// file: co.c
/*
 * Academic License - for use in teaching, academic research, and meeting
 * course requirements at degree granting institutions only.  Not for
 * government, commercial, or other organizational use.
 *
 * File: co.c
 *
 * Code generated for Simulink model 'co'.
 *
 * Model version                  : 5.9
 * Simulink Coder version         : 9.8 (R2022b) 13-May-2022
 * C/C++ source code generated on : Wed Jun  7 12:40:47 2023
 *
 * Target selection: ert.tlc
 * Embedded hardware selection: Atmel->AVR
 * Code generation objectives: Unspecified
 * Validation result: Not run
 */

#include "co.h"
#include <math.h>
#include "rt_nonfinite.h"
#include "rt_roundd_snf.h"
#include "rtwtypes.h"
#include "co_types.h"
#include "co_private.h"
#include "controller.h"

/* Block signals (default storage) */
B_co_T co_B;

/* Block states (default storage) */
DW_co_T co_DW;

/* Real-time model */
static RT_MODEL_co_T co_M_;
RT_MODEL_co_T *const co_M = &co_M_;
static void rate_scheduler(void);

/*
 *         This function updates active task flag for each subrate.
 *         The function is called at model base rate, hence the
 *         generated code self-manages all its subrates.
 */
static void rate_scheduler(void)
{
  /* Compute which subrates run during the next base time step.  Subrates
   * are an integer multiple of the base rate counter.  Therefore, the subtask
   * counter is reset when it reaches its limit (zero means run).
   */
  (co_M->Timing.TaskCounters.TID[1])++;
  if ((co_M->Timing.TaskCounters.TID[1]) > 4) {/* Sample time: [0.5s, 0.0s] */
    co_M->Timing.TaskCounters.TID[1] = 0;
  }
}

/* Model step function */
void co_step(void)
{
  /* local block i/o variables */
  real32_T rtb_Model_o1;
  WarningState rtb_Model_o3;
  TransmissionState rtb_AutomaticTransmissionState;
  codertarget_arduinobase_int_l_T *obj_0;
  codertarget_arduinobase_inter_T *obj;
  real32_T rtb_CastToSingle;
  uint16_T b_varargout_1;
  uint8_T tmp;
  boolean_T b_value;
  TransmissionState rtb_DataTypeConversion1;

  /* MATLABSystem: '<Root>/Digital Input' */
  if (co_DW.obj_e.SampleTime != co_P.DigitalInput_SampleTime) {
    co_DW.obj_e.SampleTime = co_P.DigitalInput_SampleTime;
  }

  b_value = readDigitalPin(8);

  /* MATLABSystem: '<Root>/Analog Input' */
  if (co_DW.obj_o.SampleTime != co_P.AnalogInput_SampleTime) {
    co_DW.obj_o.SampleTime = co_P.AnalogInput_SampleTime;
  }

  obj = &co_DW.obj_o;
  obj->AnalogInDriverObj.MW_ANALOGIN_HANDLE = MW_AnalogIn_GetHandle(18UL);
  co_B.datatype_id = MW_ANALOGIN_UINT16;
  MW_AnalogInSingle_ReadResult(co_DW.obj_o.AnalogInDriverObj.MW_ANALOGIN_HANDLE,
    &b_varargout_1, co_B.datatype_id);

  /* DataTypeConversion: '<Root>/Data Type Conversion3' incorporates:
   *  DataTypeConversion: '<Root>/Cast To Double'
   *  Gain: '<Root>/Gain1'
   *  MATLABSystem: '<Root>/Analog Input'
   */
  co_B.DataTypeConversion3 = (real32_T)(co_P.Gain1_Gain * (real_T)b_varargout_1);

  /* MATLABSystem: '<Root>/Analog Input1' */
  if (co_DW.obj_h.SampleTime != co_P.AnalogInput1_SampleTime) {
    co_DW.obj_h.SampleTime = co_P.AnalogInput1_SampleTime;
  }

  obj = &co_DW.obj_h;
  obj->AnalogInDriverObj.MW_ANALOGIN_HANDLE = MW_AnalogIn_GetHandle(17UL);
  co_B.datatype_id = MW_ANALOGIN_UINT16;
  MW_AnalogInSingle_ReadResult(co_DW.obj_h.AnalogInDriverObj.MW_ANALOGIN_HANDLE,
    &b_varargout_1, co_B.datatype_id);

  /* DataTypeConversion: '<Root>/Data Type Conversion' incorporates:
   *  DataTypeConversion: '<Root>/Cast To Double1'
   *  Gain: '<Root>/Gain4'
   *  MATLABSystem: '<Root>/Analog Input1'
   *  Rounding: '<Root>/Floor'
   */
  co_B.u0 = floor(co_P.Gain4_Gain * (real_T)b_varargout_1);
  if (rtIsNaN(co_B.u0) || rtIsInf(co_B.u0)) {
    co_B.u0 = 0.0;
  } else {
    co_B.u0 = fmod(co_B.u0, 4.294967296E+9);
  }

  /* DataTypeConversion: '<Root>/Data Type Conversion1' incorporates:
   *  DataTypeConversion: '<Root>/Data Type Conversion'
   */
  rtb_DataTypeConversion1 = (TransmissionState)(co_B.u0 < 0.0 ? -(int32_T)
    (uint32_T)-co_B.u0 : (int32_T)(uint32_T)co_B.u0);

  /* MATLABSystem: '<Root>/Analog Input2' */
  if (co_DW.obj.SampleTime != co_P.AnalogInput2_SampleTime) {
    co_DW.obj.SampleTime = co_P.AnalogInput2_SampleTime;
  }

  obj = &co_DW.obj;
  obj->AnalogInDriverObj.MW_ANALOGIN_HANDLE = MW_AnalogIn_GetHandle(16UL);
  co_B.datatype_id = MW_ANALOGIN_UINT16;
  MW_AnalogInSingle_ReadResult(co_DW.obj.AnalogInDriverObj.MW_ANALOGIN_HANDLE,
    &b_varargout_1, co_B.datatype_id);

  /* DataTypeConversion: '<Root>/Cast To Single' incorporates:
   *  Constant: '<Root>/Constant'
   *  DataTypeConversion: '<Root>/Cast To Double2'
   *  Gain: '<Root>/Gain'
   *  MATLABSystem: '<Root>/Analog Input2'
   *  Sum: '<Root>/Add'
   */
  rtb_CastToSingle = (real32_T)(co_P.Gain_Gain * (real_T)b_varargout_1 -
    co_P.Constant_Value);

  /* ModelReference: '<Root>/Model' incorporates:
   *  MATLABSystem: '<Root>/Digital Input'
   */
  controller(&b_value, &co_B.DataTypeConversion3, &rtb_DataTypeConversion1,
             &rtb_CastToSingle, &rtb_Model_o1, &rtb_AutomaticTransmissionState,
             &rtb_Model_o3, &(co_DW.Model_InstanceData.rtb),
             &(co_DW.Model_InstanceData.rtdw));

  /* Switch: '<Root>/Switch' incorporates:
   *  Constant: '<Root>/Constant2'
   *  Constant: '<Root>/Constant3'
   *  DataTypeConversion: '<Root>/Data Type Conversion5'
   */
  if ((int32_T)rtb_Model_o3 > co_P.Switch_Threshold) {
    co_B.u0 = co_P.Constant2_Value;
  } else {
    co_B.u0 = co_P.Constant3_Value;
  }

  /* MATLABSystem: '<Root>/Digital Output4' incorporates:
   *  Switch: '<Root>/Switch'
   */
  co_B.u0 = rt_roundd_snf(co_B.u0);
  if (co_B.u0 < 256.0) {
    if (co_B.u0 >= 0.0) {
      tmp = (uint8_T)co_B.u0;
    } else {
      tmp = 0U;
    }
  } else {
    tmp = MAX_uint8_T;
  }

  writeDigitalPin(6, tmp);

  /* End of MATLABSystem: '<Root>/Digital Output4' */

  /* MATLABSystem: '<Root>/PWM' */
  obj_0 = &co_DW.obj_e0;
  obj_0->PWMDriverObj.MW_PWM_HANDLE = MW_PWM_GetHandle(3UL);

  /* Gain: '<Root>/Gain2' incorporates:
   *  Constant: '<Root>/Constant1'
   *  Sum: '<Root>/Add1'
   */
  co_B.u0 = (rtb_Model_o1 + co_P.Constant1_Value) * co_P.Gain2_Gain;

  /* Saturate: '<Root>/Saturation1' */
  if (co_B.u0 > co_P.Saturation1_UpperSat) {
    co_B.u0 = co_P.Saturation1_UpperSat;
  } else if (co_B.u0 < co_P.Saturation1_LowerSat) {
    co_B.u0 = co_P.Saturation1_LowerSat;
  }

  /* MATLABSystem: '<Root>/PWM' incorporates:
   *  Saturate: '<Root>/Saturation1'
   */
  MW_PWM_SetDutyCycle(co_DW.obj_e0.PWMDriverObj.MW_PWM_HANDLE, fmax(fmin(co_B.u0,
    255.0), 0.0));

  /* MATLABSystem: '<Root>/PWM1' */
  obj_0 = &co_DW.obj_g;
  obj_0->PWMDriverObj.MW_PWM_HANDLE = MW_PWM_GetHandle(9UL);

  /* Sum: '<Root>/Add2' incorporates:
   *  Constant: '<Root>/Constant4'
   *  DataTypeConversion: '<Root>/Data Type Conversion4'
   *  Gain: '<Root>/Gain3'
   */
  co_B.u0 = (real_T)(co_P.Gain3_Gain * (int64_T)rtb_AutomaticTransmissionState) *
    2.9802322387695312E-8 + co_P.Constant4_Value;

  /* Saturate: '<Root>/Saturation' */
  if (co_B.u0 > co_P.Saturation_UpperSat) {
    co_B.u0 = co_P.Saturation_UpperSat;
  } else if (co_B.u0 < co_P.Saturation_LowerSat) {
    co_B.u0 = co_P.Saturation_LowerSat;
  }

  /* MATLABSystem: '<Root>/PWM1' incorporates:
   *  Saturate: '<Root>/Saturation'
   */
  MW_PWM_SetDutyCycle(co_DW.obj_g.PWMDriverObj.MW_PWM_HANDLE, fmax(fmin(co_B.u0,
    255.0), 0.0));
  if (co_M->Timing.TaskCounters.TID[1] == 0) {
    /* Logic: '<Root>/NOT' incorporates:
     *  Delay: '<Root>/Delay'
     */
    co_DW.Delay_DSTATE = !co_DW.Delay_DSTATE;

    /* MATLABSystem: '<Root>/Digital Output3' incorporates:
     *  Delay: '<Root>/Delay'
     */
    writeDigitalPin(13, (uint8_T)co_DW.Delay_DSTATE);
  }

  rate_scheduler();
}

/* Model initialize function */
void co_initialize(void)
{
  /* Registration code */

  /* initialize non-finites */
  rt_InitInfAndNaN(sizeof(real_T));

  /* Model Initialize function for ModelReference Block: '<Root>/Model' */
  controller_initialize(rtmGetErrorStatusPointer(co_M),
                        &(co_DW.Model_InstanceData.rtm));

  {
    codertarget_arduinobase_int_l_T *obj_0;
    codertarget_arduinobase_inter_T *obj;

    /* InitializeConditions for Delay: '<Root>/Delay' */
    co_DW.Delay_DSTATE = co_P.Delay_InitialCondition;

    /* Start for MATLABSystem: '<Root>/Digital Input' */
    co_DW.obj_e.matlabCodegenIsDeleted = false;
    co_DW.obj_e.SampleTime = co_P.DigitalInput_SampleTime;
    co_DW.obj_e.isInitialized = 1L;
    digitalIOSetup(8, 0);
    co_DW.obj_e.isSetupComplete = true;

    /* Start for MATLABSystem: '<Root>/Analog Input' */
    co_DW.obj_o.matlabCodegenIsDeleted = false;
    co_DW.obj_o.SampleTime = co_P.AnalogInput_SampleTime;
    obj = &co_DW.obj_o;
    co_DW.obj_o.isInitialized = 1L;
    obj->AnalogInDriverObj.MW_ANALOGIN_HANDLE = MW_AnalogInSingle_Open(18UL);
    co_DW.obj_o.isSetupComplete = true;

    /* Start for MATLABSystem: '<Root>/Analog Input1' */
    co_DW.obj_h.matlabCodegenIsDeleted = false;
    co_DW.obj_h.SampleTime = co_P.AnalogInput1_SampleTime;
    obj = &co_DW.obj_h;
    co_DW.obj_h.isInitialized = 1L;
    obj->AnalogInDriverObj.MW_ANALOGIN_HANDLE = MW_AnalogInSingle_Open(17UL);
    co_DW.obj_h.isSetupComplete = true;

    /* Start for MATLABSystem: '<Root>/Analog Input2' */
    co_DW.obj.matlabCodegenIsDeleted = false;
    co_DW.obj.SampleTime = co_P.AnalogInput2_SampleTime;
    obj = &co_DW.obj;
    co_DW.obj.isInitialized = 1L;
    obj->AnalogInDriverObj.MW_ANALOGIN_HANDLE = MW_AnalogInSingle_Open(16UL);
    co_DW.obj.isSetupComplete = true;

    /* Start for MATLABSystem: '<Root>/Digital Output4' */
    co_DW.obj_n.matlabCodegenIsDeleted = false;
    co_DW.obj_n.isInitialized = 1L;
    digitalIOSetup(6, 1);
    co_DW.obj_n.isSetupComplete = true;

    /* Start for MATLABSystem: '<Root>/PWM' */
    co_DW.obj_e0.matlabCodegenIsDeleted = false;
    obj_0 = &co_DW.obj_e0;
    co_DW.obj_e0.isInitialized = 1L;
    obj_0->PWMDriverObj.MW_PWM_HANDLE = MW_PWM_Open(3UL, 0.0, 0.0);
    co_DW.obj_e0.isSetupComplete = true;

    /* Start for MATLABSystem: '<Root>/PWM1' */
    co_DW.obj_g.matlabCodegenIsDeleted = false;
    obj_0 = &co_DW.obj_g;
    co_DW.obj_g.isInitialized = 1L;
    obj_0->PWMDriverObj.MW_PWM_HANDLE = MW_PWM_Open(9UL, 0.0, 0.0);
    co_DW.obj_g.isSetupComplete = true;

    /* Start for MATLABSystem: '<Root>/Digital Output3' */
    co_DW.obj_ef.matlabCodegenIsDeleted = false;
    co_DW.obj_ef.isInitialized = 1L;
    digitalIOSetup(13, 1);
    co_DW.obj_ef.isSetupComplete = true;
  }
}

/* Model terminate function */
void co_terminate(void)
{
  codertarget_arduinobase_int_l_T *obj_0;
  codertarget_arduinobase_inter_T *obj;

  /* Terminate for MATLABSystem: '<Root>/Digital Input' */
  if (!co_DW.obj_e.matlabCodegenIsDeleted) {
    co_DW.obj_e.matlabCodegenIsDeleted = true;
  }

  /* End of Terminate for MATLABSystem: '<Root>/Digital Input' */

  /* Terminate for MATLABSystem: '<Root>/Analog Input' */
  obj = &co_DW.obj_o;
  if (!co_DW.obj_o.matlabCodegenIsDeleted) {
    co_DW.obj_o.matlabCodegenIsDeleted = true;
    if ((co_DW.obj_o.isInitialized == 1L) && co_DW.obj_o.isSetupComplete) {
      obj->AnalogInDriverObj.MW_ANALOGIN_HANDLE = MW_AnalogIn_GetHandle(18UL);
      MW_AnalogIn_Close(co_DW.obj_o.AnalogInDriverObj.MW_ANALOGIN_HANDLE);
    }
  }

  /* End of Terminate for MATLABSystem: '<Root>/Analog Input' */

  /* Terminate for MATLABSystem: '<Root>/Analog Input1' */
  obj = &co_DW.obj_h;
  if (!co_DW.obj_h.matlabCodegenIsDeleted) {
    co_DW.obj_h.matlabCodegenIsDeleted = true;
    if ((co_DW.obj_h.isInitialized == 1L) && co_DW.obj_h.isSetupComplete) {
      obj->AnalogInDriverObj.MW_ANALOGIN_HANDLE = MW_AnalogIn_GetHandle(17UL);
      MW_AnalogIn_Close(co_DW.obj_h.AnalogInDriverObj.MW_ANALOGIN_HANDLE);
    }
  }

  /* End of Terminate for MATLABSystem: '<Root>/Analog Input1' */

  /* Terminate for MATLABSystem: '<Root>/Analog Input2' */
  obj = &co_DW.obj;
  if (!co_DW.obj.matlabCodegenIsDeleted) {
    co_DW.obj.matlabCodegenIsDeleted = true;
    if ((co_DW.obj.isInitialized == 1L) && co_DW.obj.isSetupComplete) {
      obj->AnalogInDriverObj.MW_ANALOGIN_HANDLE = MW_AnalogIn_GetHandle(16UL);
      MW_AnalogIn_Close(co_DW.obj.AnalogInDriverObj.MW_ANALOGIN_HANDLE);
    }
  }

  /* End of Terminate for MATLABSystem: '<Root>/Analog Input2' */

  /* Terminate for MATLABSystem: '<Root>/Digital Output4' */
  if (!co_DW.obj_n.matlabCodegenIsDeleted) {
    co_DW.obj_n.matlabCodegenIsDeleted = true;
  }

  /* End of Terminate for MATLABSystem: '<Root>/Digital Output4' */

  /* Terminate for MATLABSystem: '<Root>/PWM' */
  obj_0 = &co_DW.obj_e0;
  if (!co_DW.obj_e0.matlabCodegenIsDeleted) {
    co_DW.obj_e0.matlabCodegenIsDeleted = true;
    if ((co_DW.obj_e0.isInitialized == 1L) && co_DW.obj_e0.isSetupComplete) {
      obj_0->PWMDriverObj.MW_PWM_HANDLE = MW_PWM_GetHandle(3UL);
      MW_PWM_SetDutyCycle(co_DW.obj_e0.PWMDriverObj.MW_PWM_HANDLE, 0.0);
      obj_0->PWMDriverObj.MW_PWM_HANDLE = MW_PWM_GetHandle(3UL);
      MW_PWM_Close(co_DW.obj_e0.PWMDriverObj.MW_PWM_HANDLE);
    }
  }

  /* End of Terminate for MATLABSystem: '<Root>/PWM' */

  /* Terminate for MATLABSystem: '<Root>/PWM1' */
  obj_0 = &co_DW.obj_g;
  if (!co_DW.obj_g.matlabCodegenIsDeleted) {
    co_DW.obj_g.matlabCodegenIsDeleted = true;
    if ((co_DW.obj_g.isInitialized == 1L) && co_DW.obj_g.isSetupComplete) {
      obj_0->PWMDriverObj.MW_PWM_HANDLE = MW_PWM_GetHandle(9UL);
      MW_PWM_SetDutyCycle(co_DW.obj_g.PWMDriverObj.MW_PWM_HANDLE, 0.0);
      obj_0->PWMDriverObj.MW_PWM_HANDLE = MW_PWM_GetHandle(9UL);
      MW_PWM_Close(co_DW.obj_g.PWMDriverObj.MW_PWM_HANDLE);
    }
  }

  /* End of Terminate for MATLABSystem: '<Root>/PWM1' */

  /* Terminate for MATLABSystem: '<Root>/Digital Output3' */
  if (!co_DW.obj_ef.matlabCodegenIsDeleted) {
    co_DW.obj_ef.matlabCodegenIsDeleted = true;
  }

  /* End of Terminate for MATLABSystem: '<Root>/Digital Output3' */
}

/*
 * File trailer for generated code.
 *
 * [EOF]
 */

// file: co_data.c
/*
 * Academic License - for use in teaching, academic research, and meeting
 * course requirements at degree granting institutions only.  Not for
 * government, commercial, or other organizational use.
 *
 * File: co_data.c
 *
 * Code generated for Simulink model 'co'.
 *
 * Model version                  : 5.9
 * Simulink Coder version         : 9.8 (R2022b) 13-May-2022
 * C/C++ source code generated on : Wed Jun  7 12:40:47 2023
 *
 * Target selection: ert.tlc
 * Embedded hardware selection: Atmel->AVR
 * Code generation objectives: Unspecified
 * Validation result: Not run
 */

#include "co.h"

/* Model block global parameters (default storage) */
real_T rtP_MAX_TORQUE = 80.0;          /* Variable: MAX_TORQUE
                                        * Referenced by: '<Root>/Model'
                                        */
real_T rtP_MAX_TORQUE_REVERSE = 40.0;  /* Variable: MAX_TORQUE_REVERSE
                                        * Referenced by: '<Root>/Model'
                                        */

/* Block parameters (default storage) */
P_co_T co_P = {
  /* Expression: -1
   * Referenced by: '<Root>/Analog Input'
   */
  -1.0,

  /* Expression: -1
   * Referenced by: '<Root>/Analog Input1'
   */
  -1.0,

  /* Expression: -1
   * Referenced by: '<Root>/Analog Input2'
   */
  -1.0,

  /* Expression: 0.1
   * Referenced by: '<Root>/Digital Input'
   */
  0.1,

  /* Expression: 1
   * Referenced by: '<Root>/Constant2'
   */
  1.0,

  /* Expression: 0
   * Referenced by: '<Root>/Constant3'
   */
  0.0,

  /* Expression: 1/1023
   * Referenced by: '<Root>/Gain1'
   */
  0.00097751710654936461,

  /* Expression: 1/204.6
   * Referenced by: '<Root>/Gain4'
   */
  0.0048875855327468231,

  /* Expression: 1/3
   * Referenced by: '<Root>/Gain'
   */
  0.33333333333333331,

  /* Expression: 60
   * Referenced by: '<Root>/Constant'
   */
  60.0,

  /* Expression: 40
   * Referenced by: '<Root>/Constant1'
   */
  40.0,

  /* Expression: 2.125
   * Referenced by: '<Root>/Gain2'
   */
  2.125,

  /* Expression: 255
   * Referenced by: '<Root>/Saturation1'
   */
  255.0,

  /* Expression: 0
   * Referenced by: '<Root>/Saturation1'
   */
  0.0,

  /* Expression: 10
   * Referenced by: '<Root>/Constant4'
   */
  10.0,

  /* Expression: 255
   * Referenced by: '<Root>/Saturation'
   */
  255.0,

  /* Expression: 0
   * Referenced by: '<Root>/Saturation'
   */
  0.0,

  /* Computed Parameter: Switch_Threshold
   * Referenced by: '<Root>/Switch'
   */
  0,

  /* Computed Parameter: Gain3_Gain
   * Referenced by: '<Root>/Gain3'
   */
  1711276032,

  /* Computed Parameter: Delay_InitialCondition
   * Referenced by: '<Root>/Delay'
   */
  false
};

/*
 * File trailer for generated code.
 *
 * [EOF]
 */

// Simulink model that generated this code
simulink model "co"  (R2022b)
settings: Solver=FixedStepAuto  StartTime=0.0  StopTime=10.0  FixedStep=1/10  RelTol=1e-3
InitFcn:
  | init_fn
libraries: arduinolib x8

== system co ==
  Add : Sum  Inputs=+-
  Add1 : Sum
  Add2 : Sum
  Analog Input : arduinolib/Analog Input  pinNumber=4  ReadResultsOnly=off  ConversionTriggerSource=Software  ExternalTriggerType=uint32( 0 )  OutputDataType=uint16  EnableConversionCompleteNotify=off  EnableOuputStatus=off  SampleTime=-1  blockPlatform=arduino
  Analog Input1 : arduinolib/Analog Input  pinNumber=3  ReadResultsOnly=off  ConversionTriggerSource=Software  ExternalTriggerType=uint32( 0 )  OutputDataType=uint16  EnableConversionCompleteNotify=off  EnableOuputStatus=off  SampleTime=-1  blockPlatform=arduino
  Analog Input2 : arduinolib/Analog Input  pinNumber=2  ReadResultsOnly=off  ConversionTriggerSource=Software  ExternalTriggerType=uint32( 0 )  OutputDataType=uint16  EnableConversionCompleteNotify=off  EnableOuputStatus=off  SampleTime=-1  blockPlatform=arduino
  Cast To Double : DataTypeConversion  OutDataTypeStr=double  SaturateOnIntegerOverflow=off  RndMeth=Floor
  Cast To Double1 : DataTypeConversion  OutDataTypeStr=double  SaturateOnIntegerOverflow=off  RndMeth=Floor
  Cast To Double2 : DataTypeConversion  OutDataTypeStr=double  SaturateOnIntegerOverflow=off  RndMeth=Floor
  Cast To Single : DataTypeConversion  OutDataTypeStr=single  SaturateOnIntegerOverflow=off  RndMeth=Floor
  Constant : Constant  Value=60
  Constant1 : Constant  Value=40
  Constant2 : Constant
  Constant3 : Constant  Value=0
  Constant4 : Constant  Value=10
  Data Type Conversion : DataTypeConversion  OutDataTypeStr=int32  SaturateOnIntegerOverflow=off  RndMeth=Floor
  Data Type Conversion1 : DataTypeConversion  OutDataTypeStr=Enum: TransmissionState  SaturateOnIntegerOverflow=off  RndMeth=Floor
  Data Type Conversion2 : DataTypeConversion  OutDataTypeStr=boolean  SaturateOnIntegerOverflow=off  RndMeth=Floor
  Data Type Conversion3 : DataTypeConversion  OutDataTypeStr=single  SaturateOnIntegerOverflow=off  RndMeth=Floor
  Data Type Conversion4 : DataTypeConversion  OutDataTypeStr=int32  SaturateOnIntegerOverflow=off  RndMeth=Floor
  Data Type Conversion5 : DataTypeConversion  OutDataTypeStr=int32  SaturateOnIntegerOverflow=off  RndMeth=Floor
  Delay : Delay  DelayLength=1  SampleTime=0.5
  Digital Input : arduinolib/Digital Input  pinNumber=8  mode=Default  Direction=input  SampleTime=0.1  blockPlatform=arduino
  Digital Output3 : arduinolib/Digital Output  pinNumber=13  Direction=output  blockPlatform=arduino
  Digital Output4 : arduinolib/Digital Output  pinNumber=6  Direction=output  blockPlatform=arduino
  Floor : Rounding
  Gain : Gain  Gain=1/3
  Gain1 : Gain  Gain=1/1023
  Gain2 : Gain  Gain=2.125
  Gain3 : Gain  Gain=51
  Gain4 : Gain  Gain=1/204.6
  Model : ModelReference  ModelNameDialog=controller  SimulationMode=Normal  ModelReferenceVersion=3.67
  NOT : Logic  Operator=NOT  IconShape=distinctive  AllPortsSameDT=off  OutDataTypeStr=boolean
  PWM : arduinolib/PWM  pinNumber=3  frequencyType=Default  desiredFrequency=490.2  achievableFrequency=490.2
  PWM1 : arduinolib/PWM  pinNumber=9  frequencyType=Default  desiredFrequency=490.2  achievableFrequency=490.2
  Saturation : Saturate  UpperLimit=255  LowerLimit=0
  Saturation1 : Saturate  UpperLimit=255  LowerLimit=0
  Scope : Scope
  Switch : Switch  Criteria=u2 > Threshold  SaturateOnIntegerOverflow=off  InputSameDT=off
  wires:
  NOT/1 -> Delay/1, Scope/1, Digital Output3/1
  Delay/1 -> NOT/1
  Cast To Double/1 -> Gain1/1
  Floor/1 -> Data Type Conversion/1
  Analog Input2/1 -> Cast To Double2/1
  Analog Input1/1 -> Cast To Double1/1
  Gain1/1 -> Data Type Conversion3/1
  Gain/1 -> Add/1
  Analog Input/1 -> Cast To Double/1
  Constant/1 -> Add/2
  Data Type Conversion/1 -> Data Type Conversion1/1
  Add/1 -> Cast To Single/1
  Digital Input/1 -> Data Type Conversion2/1
  Cast To Single/1 -> Model/4
  Data Type Conversion1/1 -> Model/3
  Data Type Conversion5/1 -> Switch/2
  Saturation/1 -> PWM1/1
  Model/2 -> Data Type Conversion4/1  "AutomaticTransmissionState"
  Switch/1 -> Digital Output4/1
  Constant3/1 -> Switch/3
  Model/3 -> Data Type Conversion5/1
  Constant2/1 -> Switch/1
  Gain3/1 -> Add2/1
  Add1/1 -> Gain2/1
  Saturation1/1 -> PWM/1
  Model/1 -> Add1/1
  Constant1/1 -> Add1/2
  Data Type Conversion4/1 -> Gain3/1
  Data Type Conversion3/1 -> Model/2
  Data Type Conversion2/1 -> Model/1
  Cast To Double1/1 -> Gain4/1
  Gain4/1 -> Floor/1
  Cast To Double2/1 -> Gain/1
  Gain2/1 -> Saturation1/1
  Constant4/1 -> Add2/2
  Add2/1 -> Saturation/1
